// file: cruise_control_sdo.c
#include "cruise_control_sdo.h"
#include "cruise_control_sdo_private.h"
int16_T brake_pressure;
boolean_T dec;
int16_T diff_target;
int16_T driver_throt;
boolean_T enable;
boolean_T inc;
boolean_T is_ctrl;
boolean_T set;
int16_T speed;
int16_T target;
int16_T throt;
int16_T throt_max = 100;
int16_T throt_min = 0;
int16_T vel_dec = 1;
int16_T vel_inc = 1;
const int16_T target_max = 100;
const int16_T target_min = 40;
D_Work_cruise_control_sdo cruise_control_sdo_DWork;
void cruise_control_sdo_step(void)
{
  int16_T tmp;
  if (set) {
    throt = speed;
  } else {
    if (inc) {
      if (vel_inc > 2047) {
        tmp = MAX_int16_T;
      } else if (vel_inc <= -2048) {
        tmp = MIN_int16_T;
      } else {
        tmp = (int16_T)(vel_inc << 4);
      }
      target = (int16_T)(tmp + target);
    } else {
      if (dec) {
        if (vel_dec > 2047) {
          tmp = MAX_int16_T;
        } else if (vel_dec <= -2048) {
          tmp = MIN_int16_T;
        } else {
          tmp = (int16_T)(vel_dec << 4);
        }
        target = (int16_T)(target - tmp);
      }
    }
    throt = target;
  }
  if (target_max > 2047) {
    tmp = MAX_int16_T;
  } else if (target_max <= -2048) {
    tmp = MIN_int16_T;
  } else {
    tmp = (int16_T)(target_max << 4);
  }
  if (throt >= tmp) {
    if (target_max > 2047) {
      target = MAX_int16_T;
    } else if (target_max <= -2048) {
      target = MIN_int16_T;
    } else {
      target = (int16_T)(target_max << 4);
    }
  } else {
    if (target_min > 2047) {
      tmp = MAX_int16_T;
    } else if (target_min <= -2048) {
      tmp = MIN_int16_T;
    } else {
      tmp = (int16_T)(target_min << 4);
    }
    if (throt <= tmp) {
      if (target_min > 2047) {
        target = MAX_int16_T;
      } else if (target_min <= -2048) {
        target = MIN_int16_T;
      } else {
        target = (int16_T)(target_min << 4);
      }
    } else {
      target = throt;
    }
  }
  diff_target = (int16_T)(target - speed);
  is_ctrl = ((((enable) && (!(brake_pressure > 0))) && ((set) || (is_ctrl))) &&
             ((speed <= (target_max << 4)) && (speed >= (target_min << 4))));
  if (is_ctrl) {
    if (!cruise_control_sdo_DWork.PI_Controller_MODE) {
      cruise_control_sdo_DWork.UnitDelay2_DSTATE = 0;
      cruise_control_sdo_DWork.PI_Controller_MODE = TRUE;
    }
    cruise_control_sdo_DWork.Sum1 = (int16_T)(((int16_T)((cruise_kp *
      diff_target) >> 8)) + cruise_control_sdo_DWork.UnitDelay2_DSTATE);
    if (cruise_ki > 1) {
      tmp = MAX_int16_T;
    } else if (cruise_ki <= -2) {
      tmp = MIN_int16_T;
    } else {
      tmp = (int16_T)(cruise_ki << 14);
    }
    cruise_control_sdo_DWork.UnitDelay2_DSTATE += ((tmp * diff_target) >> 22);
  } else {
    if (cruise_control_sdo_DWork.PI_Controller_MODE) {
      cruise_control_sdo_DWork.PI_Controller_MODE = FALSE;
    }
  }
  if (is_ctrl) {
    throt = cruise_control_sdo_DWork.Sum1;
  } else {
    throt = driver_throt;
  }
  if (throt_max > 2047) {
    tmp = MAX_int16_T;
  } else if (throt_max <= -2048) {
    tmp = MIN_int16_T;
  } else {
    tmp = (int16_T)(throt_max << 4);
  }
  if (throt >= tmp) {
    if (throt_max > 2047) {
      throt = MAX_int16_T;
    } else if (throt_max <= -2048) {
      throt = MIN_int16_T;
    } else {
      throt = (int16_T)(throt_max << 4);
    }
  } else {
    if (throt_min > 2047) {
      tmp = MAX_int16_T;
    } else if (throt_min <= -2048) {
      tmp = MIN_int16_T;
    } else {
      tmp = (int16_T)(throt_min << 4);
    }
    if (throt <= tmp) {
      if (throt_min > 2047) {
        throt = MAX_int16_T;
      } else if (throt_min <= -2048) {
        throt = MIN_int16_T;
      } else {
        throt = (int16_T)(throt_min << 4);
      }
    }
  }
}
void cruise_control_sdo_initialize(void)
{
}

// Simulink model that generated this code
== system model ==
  enable : Inport
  brake_pressure : Inport
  set : Inport
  inc : Inport
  dec : Inport
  driver_throt : Inport
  speed : Inport
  throt : Outport  <- 1: Saturate#1
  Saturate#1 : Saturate  UpperLimit=throt_max  LowerLimit=throt_min  <- 1: Switch#1
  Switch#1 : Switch  Criteria=u2 ~= 0  <- 1: PI_Controller, 2: Logic#1, 3: driver_throt
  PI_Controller : Subsystem  <- 1: Sum1, Enable: Logic#1
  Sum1 : Sum  Inputs=-+  <- 1: speed, 2: Saturate#2
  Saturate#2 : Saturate  UpperLimit=target_max  LowerLimit=target_min  <- 1: Switch#2
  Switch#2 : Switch  Criteria=u2 ~= 0  <- 1: speed, 2: set, 3: Switch#3
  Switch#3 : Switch  Criteria=u2 ~= 0  <- 1: Sum#1, 2: inc, 3: Switch#4
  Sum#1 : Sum  <- 1: Constant#1, 2: UnitDelay#1
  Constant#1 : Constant  Value=vel_inc
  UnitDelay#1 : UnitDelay  <- 1: Saturate#2
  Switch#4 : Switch  Criteria=u2 ~= 0  <- 1: Sum#2, 2: dec, 3: UnitDelay#1
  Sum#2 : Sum  Inputs=-+  <- 1: Constant#2, 2: UnitDelay#1
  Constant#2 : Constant  Value=vel_dec
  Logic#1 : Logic  Inputs=4  <- 1: enable, 2: Logic#2, 3: Logic#3, 4: Logic#4
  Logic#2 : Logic  Operator=NOT  <- 1: CompareToConstant#1
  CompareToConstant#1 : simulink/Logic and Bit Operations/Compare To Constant  relop=>  const=0  <- 1: brake_pressure
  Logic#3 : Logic  Operator=OR  <- 1: set, 2: UnitDelay#2
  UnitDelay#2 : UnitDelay  <- 1: Logic#1
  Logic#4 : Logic  <- 1: RelationalOperator#1, 2: RelationalOperator#2
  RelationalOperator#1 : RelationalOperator  Operator=<=  <- 1: speed, 2: Constant#3
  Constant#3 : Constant  Value=target_max
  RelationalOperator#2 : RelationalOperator  <- 1: speed, 2: Constant#4
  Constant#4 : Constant  Value=target_min
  target : Outport  <- 1: Saturate#2
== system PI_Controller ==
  diff_target : Inport
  is_ctrl : EnablePort
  Outport#1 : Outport  <- 1: Sum#3
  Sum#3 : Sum  <- 1: Gain#1, 2: UnitDelay2
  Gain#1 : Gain  Gain=cruise_kp  <- 1: diff_target
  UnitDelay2 : UnitDelay  <- 1: Sum#4
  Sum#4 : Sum  <- 1: Gain#2, 2: UnitDelay2
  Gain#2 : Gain  Gain=cruise_ki  <- 1: diff_target
